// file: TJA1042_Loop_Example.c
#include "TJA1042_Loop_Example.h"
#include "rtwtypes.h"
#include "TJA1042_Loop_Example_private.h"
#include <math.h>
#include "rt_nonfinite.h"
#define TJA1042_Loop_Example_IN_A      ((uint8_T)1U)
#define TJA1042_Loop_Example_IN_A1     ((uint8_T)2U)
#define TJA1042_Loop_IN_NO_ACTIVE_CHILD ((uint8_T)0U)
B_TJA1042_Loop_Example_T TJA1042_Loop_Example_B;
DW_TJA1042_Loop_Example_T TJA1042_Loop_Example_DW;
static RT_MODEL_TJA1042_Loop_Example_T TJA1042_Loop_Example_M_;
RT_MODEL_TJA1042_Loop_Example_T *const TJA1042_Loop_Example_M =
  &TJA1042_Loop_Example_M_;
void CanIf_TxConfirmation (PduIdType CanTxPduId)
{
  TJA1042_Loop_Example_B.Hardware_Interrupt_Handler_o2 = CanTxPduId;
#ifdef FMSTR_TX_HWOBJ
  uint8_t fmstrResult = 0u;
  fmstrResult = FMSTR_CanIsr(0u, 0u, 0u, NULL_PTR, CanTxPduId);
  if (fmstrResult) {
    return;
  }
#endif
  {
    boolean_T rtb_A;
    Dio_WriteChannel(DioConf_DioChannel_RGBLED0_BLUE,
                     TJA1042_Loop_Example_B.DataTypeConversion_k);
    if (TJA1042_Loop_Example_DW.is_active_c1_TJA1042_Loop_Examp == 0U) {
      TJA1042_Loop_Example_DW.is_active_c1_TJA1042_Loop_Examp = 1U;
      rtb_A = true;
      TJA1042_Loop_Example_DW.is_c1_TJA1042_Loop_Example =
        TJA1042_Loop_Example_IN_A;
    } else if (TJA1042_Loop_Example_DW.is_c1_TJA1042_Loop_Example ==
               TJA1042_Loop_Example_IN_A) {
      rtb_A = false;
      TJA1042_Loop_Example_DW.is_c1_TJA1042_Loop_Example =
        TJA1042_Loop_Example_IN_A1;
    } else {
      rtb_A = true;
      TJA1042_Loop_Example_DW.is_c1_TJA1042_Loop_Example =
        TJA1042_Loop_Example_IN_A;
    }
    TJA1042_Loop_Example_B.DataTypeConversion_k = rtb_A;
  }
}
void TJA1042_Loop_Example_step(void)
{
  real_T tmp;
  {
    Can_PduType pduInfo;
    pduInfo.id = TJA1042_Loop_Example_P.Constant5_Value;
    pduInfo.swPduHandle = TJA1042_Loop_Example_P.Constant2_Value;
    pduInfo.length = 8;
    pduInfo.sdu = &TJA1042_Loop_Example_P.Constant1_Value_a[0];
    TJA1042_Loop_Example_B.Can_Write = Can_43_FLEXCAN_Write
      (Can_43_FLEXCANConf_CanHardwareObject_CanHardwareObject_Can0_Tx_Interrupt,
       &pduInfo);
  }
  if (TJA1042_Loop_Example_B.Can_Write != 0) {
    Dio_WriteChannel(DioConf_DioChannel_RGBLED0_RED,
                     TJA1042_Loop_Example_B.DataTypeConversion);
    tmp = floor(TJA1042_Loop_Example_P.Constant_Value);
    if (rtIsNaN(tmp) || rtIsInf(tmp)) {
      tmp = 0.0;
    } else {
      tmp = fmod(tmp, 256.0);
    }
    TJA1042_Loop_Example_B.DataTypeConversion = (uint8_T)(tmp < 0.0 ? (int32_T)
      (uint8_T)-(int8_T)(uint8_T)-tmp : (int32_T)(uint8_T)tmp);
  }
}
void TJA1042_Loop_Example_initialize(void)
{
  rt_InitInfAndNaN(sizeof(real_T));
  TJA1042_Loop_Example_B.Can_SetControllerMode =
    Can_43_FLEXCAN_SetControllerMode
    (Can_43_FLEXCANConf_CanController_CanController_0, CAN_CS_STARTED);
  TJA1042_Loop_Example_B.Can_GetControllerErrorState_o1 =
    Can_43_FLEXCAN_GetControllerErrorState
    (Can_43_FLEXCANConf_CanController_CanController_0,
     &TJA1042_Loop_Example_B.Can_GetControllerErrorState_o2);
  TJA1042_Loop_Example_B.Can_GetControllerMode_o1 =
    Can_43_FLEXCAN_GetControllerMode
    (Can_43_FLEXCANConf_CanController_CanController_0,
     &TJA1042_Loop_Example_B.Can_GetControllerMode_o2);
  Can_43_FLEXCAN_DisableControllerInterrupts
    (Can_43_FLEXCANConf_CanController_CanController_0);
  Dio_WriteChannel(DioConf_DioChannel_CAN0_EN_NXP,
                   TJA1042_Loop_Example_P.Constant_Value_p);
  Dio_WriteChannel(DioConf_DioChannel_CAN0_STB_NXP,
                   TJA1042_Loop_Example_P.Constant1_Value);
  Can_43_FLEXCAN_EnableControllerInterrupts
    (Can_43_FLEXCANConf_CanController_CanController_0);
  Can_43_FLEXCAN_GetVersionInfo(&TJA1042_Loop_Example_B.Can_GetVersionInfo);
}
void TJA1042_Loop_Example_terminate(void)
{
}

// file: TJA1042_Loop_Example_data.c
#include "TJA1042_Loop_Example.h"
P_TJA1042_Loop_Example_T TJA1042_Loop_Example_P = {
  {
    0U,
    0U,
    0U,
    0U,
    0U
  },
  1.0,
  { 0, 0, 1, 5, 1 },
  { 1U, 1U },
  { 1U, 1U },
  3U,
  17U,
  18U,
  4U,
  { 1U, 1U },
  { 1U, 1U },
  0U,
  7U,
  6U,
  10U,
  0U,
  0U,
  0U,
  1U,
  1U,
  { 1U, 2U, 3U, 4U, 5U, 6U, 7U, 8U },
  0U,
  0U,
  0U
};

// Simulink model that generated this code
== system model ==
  Subsystem#1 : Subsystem  <- Trigger: Hardware_Interrupt_Handler
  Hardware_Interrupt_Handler : mbd_s32k3_isr_library/Hardware_Interrupt_Handler
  Subsystem#2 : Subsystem  <- Action: If#1
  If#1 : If  IfExpression=u1 ~= 0  <- 1: Can_Write
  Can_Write : mbd_s32k3_communication_library/Can  <- 1: Constant5, 2: Constant2, 3: Constant1
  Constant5 : Constant  Value=10
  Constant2 : Constant  Value=0
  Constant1 : Constant  Value=[1 2 3 4 5 6 7 8]
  Subsystem#3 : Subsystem
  DataStoreMemory#1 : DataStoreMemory  DataStoreName=GetVersionInfo_VersionInfo
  DataStoreMemory#2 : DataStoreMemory  DataStoreName=GetControllerMode_Mode
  DataStoreMemory#3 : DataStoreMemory  DataStoreName=GetControllerErrorState_State
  DataStoreMemory#4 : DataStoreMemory  DataStoreName=SetControllerMode_Status
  DataStoreMemory#5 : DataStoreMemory  DataStoreName=GetControllerMode_Status
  DataStoreMemory#6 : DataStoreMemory  DataStoreName=GetControllerErrorState_Status
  CustomCallbackButton#1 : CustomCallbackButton
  CustomCallbackButton#2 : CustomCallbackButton
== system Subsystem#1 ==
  TriggerPort#1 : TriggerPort  TriggerType=function-call
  Dio_WriteChannel : mbd_s32k3_io_library/Dio  <- 1: DataTypeConversion
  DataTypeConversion : DataTypeConversion  <- 1: Stateflowchart#1
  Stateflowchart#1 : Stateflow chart
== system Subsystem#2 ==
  ActionPort#1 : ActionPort
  Dio#1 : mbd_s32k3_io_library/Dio  <- 1: DataTypeConversion#1
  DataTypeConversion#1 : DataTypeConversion  <- 1: Constant
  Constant : Constant
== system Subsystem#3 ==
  Dio#2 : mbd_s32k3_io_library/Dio  <- 1: Constant#1
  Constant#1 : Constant
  Constant#2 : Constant  Value=3
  Constant#3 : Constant  Value=6
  Subsystem#4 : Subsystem  <- Action: If#2
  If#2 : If  IfExpression=u1 ~= 0  <- 1: MATLABFunction#1
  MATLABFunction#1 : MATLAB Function  <- 2: Constant#4, 3: Constant#5, 4: Constant#6
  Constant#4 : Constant  Value=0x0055
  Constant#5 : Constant  Value=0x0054
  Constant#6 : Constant  Value=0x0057
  DataStoreWrite#1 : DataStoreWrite  DataStoreName=SetControllerMode_Status  Indices=1  <- 1: Can_SetControllerMode
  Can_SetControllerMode : mbd_s32k3_communication_library/Can
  DataStoreWrite#2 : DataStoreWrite  DataStoreName=GetControllerErrorState_Status  Indices=1  <- 1: Can_GetControllerErrorState
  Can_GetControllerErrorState : mbd_s32k3_communication_library/Can
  DataStoreWrite#3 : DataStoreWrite  DataStoreName=GetControllerErrorState_State  Indices=1  <- 1: Can_GetControllerErrorState/2
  DataStoreWrite#4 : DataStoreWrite  DataStoreName=GetControllerMode_Status  Indices=1  <- 1: Can_GetControllerMode
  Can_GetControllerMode : mbd_s32k3_communication_library/Can
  DataStoreWrite#5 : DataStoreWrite  DataStoreName=GetControllerMode_Mode  Indices=1  <- 1: Can_GetControllerMode/2
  Can#1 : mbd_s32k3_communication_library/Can
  Dio#3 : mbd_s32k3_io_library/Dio  <- 1: Constant#7
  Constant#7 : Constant
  Can#2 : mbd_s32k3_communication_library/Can
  DataStoreWrite#6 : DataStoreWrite  DataStoreName=GetVersionInfo_VersionInfo  Indices=1  <- 1: Can_GetVersionInfo
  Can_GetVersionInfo : mbd_s32k3_communication_library/Can
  EventListener#1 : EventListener
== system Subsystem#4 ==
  ActionPort#2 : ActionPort
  Dio#4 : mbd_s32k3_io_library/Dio  <- 1: Constant#8
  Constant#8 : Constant
== matlab function MATLABFunction#1 ==
function status = TJA1153_Init(canExtHwId, canEnDioChannel, canStbDioChannel, canErrnDioChannel)

	status = mbd_s32k3.common.nxp.can.TJA1153Transceiver.init(canExtHwId, canEnDioChannel, canStbDioChannel, canErrnDioChannel);

end
